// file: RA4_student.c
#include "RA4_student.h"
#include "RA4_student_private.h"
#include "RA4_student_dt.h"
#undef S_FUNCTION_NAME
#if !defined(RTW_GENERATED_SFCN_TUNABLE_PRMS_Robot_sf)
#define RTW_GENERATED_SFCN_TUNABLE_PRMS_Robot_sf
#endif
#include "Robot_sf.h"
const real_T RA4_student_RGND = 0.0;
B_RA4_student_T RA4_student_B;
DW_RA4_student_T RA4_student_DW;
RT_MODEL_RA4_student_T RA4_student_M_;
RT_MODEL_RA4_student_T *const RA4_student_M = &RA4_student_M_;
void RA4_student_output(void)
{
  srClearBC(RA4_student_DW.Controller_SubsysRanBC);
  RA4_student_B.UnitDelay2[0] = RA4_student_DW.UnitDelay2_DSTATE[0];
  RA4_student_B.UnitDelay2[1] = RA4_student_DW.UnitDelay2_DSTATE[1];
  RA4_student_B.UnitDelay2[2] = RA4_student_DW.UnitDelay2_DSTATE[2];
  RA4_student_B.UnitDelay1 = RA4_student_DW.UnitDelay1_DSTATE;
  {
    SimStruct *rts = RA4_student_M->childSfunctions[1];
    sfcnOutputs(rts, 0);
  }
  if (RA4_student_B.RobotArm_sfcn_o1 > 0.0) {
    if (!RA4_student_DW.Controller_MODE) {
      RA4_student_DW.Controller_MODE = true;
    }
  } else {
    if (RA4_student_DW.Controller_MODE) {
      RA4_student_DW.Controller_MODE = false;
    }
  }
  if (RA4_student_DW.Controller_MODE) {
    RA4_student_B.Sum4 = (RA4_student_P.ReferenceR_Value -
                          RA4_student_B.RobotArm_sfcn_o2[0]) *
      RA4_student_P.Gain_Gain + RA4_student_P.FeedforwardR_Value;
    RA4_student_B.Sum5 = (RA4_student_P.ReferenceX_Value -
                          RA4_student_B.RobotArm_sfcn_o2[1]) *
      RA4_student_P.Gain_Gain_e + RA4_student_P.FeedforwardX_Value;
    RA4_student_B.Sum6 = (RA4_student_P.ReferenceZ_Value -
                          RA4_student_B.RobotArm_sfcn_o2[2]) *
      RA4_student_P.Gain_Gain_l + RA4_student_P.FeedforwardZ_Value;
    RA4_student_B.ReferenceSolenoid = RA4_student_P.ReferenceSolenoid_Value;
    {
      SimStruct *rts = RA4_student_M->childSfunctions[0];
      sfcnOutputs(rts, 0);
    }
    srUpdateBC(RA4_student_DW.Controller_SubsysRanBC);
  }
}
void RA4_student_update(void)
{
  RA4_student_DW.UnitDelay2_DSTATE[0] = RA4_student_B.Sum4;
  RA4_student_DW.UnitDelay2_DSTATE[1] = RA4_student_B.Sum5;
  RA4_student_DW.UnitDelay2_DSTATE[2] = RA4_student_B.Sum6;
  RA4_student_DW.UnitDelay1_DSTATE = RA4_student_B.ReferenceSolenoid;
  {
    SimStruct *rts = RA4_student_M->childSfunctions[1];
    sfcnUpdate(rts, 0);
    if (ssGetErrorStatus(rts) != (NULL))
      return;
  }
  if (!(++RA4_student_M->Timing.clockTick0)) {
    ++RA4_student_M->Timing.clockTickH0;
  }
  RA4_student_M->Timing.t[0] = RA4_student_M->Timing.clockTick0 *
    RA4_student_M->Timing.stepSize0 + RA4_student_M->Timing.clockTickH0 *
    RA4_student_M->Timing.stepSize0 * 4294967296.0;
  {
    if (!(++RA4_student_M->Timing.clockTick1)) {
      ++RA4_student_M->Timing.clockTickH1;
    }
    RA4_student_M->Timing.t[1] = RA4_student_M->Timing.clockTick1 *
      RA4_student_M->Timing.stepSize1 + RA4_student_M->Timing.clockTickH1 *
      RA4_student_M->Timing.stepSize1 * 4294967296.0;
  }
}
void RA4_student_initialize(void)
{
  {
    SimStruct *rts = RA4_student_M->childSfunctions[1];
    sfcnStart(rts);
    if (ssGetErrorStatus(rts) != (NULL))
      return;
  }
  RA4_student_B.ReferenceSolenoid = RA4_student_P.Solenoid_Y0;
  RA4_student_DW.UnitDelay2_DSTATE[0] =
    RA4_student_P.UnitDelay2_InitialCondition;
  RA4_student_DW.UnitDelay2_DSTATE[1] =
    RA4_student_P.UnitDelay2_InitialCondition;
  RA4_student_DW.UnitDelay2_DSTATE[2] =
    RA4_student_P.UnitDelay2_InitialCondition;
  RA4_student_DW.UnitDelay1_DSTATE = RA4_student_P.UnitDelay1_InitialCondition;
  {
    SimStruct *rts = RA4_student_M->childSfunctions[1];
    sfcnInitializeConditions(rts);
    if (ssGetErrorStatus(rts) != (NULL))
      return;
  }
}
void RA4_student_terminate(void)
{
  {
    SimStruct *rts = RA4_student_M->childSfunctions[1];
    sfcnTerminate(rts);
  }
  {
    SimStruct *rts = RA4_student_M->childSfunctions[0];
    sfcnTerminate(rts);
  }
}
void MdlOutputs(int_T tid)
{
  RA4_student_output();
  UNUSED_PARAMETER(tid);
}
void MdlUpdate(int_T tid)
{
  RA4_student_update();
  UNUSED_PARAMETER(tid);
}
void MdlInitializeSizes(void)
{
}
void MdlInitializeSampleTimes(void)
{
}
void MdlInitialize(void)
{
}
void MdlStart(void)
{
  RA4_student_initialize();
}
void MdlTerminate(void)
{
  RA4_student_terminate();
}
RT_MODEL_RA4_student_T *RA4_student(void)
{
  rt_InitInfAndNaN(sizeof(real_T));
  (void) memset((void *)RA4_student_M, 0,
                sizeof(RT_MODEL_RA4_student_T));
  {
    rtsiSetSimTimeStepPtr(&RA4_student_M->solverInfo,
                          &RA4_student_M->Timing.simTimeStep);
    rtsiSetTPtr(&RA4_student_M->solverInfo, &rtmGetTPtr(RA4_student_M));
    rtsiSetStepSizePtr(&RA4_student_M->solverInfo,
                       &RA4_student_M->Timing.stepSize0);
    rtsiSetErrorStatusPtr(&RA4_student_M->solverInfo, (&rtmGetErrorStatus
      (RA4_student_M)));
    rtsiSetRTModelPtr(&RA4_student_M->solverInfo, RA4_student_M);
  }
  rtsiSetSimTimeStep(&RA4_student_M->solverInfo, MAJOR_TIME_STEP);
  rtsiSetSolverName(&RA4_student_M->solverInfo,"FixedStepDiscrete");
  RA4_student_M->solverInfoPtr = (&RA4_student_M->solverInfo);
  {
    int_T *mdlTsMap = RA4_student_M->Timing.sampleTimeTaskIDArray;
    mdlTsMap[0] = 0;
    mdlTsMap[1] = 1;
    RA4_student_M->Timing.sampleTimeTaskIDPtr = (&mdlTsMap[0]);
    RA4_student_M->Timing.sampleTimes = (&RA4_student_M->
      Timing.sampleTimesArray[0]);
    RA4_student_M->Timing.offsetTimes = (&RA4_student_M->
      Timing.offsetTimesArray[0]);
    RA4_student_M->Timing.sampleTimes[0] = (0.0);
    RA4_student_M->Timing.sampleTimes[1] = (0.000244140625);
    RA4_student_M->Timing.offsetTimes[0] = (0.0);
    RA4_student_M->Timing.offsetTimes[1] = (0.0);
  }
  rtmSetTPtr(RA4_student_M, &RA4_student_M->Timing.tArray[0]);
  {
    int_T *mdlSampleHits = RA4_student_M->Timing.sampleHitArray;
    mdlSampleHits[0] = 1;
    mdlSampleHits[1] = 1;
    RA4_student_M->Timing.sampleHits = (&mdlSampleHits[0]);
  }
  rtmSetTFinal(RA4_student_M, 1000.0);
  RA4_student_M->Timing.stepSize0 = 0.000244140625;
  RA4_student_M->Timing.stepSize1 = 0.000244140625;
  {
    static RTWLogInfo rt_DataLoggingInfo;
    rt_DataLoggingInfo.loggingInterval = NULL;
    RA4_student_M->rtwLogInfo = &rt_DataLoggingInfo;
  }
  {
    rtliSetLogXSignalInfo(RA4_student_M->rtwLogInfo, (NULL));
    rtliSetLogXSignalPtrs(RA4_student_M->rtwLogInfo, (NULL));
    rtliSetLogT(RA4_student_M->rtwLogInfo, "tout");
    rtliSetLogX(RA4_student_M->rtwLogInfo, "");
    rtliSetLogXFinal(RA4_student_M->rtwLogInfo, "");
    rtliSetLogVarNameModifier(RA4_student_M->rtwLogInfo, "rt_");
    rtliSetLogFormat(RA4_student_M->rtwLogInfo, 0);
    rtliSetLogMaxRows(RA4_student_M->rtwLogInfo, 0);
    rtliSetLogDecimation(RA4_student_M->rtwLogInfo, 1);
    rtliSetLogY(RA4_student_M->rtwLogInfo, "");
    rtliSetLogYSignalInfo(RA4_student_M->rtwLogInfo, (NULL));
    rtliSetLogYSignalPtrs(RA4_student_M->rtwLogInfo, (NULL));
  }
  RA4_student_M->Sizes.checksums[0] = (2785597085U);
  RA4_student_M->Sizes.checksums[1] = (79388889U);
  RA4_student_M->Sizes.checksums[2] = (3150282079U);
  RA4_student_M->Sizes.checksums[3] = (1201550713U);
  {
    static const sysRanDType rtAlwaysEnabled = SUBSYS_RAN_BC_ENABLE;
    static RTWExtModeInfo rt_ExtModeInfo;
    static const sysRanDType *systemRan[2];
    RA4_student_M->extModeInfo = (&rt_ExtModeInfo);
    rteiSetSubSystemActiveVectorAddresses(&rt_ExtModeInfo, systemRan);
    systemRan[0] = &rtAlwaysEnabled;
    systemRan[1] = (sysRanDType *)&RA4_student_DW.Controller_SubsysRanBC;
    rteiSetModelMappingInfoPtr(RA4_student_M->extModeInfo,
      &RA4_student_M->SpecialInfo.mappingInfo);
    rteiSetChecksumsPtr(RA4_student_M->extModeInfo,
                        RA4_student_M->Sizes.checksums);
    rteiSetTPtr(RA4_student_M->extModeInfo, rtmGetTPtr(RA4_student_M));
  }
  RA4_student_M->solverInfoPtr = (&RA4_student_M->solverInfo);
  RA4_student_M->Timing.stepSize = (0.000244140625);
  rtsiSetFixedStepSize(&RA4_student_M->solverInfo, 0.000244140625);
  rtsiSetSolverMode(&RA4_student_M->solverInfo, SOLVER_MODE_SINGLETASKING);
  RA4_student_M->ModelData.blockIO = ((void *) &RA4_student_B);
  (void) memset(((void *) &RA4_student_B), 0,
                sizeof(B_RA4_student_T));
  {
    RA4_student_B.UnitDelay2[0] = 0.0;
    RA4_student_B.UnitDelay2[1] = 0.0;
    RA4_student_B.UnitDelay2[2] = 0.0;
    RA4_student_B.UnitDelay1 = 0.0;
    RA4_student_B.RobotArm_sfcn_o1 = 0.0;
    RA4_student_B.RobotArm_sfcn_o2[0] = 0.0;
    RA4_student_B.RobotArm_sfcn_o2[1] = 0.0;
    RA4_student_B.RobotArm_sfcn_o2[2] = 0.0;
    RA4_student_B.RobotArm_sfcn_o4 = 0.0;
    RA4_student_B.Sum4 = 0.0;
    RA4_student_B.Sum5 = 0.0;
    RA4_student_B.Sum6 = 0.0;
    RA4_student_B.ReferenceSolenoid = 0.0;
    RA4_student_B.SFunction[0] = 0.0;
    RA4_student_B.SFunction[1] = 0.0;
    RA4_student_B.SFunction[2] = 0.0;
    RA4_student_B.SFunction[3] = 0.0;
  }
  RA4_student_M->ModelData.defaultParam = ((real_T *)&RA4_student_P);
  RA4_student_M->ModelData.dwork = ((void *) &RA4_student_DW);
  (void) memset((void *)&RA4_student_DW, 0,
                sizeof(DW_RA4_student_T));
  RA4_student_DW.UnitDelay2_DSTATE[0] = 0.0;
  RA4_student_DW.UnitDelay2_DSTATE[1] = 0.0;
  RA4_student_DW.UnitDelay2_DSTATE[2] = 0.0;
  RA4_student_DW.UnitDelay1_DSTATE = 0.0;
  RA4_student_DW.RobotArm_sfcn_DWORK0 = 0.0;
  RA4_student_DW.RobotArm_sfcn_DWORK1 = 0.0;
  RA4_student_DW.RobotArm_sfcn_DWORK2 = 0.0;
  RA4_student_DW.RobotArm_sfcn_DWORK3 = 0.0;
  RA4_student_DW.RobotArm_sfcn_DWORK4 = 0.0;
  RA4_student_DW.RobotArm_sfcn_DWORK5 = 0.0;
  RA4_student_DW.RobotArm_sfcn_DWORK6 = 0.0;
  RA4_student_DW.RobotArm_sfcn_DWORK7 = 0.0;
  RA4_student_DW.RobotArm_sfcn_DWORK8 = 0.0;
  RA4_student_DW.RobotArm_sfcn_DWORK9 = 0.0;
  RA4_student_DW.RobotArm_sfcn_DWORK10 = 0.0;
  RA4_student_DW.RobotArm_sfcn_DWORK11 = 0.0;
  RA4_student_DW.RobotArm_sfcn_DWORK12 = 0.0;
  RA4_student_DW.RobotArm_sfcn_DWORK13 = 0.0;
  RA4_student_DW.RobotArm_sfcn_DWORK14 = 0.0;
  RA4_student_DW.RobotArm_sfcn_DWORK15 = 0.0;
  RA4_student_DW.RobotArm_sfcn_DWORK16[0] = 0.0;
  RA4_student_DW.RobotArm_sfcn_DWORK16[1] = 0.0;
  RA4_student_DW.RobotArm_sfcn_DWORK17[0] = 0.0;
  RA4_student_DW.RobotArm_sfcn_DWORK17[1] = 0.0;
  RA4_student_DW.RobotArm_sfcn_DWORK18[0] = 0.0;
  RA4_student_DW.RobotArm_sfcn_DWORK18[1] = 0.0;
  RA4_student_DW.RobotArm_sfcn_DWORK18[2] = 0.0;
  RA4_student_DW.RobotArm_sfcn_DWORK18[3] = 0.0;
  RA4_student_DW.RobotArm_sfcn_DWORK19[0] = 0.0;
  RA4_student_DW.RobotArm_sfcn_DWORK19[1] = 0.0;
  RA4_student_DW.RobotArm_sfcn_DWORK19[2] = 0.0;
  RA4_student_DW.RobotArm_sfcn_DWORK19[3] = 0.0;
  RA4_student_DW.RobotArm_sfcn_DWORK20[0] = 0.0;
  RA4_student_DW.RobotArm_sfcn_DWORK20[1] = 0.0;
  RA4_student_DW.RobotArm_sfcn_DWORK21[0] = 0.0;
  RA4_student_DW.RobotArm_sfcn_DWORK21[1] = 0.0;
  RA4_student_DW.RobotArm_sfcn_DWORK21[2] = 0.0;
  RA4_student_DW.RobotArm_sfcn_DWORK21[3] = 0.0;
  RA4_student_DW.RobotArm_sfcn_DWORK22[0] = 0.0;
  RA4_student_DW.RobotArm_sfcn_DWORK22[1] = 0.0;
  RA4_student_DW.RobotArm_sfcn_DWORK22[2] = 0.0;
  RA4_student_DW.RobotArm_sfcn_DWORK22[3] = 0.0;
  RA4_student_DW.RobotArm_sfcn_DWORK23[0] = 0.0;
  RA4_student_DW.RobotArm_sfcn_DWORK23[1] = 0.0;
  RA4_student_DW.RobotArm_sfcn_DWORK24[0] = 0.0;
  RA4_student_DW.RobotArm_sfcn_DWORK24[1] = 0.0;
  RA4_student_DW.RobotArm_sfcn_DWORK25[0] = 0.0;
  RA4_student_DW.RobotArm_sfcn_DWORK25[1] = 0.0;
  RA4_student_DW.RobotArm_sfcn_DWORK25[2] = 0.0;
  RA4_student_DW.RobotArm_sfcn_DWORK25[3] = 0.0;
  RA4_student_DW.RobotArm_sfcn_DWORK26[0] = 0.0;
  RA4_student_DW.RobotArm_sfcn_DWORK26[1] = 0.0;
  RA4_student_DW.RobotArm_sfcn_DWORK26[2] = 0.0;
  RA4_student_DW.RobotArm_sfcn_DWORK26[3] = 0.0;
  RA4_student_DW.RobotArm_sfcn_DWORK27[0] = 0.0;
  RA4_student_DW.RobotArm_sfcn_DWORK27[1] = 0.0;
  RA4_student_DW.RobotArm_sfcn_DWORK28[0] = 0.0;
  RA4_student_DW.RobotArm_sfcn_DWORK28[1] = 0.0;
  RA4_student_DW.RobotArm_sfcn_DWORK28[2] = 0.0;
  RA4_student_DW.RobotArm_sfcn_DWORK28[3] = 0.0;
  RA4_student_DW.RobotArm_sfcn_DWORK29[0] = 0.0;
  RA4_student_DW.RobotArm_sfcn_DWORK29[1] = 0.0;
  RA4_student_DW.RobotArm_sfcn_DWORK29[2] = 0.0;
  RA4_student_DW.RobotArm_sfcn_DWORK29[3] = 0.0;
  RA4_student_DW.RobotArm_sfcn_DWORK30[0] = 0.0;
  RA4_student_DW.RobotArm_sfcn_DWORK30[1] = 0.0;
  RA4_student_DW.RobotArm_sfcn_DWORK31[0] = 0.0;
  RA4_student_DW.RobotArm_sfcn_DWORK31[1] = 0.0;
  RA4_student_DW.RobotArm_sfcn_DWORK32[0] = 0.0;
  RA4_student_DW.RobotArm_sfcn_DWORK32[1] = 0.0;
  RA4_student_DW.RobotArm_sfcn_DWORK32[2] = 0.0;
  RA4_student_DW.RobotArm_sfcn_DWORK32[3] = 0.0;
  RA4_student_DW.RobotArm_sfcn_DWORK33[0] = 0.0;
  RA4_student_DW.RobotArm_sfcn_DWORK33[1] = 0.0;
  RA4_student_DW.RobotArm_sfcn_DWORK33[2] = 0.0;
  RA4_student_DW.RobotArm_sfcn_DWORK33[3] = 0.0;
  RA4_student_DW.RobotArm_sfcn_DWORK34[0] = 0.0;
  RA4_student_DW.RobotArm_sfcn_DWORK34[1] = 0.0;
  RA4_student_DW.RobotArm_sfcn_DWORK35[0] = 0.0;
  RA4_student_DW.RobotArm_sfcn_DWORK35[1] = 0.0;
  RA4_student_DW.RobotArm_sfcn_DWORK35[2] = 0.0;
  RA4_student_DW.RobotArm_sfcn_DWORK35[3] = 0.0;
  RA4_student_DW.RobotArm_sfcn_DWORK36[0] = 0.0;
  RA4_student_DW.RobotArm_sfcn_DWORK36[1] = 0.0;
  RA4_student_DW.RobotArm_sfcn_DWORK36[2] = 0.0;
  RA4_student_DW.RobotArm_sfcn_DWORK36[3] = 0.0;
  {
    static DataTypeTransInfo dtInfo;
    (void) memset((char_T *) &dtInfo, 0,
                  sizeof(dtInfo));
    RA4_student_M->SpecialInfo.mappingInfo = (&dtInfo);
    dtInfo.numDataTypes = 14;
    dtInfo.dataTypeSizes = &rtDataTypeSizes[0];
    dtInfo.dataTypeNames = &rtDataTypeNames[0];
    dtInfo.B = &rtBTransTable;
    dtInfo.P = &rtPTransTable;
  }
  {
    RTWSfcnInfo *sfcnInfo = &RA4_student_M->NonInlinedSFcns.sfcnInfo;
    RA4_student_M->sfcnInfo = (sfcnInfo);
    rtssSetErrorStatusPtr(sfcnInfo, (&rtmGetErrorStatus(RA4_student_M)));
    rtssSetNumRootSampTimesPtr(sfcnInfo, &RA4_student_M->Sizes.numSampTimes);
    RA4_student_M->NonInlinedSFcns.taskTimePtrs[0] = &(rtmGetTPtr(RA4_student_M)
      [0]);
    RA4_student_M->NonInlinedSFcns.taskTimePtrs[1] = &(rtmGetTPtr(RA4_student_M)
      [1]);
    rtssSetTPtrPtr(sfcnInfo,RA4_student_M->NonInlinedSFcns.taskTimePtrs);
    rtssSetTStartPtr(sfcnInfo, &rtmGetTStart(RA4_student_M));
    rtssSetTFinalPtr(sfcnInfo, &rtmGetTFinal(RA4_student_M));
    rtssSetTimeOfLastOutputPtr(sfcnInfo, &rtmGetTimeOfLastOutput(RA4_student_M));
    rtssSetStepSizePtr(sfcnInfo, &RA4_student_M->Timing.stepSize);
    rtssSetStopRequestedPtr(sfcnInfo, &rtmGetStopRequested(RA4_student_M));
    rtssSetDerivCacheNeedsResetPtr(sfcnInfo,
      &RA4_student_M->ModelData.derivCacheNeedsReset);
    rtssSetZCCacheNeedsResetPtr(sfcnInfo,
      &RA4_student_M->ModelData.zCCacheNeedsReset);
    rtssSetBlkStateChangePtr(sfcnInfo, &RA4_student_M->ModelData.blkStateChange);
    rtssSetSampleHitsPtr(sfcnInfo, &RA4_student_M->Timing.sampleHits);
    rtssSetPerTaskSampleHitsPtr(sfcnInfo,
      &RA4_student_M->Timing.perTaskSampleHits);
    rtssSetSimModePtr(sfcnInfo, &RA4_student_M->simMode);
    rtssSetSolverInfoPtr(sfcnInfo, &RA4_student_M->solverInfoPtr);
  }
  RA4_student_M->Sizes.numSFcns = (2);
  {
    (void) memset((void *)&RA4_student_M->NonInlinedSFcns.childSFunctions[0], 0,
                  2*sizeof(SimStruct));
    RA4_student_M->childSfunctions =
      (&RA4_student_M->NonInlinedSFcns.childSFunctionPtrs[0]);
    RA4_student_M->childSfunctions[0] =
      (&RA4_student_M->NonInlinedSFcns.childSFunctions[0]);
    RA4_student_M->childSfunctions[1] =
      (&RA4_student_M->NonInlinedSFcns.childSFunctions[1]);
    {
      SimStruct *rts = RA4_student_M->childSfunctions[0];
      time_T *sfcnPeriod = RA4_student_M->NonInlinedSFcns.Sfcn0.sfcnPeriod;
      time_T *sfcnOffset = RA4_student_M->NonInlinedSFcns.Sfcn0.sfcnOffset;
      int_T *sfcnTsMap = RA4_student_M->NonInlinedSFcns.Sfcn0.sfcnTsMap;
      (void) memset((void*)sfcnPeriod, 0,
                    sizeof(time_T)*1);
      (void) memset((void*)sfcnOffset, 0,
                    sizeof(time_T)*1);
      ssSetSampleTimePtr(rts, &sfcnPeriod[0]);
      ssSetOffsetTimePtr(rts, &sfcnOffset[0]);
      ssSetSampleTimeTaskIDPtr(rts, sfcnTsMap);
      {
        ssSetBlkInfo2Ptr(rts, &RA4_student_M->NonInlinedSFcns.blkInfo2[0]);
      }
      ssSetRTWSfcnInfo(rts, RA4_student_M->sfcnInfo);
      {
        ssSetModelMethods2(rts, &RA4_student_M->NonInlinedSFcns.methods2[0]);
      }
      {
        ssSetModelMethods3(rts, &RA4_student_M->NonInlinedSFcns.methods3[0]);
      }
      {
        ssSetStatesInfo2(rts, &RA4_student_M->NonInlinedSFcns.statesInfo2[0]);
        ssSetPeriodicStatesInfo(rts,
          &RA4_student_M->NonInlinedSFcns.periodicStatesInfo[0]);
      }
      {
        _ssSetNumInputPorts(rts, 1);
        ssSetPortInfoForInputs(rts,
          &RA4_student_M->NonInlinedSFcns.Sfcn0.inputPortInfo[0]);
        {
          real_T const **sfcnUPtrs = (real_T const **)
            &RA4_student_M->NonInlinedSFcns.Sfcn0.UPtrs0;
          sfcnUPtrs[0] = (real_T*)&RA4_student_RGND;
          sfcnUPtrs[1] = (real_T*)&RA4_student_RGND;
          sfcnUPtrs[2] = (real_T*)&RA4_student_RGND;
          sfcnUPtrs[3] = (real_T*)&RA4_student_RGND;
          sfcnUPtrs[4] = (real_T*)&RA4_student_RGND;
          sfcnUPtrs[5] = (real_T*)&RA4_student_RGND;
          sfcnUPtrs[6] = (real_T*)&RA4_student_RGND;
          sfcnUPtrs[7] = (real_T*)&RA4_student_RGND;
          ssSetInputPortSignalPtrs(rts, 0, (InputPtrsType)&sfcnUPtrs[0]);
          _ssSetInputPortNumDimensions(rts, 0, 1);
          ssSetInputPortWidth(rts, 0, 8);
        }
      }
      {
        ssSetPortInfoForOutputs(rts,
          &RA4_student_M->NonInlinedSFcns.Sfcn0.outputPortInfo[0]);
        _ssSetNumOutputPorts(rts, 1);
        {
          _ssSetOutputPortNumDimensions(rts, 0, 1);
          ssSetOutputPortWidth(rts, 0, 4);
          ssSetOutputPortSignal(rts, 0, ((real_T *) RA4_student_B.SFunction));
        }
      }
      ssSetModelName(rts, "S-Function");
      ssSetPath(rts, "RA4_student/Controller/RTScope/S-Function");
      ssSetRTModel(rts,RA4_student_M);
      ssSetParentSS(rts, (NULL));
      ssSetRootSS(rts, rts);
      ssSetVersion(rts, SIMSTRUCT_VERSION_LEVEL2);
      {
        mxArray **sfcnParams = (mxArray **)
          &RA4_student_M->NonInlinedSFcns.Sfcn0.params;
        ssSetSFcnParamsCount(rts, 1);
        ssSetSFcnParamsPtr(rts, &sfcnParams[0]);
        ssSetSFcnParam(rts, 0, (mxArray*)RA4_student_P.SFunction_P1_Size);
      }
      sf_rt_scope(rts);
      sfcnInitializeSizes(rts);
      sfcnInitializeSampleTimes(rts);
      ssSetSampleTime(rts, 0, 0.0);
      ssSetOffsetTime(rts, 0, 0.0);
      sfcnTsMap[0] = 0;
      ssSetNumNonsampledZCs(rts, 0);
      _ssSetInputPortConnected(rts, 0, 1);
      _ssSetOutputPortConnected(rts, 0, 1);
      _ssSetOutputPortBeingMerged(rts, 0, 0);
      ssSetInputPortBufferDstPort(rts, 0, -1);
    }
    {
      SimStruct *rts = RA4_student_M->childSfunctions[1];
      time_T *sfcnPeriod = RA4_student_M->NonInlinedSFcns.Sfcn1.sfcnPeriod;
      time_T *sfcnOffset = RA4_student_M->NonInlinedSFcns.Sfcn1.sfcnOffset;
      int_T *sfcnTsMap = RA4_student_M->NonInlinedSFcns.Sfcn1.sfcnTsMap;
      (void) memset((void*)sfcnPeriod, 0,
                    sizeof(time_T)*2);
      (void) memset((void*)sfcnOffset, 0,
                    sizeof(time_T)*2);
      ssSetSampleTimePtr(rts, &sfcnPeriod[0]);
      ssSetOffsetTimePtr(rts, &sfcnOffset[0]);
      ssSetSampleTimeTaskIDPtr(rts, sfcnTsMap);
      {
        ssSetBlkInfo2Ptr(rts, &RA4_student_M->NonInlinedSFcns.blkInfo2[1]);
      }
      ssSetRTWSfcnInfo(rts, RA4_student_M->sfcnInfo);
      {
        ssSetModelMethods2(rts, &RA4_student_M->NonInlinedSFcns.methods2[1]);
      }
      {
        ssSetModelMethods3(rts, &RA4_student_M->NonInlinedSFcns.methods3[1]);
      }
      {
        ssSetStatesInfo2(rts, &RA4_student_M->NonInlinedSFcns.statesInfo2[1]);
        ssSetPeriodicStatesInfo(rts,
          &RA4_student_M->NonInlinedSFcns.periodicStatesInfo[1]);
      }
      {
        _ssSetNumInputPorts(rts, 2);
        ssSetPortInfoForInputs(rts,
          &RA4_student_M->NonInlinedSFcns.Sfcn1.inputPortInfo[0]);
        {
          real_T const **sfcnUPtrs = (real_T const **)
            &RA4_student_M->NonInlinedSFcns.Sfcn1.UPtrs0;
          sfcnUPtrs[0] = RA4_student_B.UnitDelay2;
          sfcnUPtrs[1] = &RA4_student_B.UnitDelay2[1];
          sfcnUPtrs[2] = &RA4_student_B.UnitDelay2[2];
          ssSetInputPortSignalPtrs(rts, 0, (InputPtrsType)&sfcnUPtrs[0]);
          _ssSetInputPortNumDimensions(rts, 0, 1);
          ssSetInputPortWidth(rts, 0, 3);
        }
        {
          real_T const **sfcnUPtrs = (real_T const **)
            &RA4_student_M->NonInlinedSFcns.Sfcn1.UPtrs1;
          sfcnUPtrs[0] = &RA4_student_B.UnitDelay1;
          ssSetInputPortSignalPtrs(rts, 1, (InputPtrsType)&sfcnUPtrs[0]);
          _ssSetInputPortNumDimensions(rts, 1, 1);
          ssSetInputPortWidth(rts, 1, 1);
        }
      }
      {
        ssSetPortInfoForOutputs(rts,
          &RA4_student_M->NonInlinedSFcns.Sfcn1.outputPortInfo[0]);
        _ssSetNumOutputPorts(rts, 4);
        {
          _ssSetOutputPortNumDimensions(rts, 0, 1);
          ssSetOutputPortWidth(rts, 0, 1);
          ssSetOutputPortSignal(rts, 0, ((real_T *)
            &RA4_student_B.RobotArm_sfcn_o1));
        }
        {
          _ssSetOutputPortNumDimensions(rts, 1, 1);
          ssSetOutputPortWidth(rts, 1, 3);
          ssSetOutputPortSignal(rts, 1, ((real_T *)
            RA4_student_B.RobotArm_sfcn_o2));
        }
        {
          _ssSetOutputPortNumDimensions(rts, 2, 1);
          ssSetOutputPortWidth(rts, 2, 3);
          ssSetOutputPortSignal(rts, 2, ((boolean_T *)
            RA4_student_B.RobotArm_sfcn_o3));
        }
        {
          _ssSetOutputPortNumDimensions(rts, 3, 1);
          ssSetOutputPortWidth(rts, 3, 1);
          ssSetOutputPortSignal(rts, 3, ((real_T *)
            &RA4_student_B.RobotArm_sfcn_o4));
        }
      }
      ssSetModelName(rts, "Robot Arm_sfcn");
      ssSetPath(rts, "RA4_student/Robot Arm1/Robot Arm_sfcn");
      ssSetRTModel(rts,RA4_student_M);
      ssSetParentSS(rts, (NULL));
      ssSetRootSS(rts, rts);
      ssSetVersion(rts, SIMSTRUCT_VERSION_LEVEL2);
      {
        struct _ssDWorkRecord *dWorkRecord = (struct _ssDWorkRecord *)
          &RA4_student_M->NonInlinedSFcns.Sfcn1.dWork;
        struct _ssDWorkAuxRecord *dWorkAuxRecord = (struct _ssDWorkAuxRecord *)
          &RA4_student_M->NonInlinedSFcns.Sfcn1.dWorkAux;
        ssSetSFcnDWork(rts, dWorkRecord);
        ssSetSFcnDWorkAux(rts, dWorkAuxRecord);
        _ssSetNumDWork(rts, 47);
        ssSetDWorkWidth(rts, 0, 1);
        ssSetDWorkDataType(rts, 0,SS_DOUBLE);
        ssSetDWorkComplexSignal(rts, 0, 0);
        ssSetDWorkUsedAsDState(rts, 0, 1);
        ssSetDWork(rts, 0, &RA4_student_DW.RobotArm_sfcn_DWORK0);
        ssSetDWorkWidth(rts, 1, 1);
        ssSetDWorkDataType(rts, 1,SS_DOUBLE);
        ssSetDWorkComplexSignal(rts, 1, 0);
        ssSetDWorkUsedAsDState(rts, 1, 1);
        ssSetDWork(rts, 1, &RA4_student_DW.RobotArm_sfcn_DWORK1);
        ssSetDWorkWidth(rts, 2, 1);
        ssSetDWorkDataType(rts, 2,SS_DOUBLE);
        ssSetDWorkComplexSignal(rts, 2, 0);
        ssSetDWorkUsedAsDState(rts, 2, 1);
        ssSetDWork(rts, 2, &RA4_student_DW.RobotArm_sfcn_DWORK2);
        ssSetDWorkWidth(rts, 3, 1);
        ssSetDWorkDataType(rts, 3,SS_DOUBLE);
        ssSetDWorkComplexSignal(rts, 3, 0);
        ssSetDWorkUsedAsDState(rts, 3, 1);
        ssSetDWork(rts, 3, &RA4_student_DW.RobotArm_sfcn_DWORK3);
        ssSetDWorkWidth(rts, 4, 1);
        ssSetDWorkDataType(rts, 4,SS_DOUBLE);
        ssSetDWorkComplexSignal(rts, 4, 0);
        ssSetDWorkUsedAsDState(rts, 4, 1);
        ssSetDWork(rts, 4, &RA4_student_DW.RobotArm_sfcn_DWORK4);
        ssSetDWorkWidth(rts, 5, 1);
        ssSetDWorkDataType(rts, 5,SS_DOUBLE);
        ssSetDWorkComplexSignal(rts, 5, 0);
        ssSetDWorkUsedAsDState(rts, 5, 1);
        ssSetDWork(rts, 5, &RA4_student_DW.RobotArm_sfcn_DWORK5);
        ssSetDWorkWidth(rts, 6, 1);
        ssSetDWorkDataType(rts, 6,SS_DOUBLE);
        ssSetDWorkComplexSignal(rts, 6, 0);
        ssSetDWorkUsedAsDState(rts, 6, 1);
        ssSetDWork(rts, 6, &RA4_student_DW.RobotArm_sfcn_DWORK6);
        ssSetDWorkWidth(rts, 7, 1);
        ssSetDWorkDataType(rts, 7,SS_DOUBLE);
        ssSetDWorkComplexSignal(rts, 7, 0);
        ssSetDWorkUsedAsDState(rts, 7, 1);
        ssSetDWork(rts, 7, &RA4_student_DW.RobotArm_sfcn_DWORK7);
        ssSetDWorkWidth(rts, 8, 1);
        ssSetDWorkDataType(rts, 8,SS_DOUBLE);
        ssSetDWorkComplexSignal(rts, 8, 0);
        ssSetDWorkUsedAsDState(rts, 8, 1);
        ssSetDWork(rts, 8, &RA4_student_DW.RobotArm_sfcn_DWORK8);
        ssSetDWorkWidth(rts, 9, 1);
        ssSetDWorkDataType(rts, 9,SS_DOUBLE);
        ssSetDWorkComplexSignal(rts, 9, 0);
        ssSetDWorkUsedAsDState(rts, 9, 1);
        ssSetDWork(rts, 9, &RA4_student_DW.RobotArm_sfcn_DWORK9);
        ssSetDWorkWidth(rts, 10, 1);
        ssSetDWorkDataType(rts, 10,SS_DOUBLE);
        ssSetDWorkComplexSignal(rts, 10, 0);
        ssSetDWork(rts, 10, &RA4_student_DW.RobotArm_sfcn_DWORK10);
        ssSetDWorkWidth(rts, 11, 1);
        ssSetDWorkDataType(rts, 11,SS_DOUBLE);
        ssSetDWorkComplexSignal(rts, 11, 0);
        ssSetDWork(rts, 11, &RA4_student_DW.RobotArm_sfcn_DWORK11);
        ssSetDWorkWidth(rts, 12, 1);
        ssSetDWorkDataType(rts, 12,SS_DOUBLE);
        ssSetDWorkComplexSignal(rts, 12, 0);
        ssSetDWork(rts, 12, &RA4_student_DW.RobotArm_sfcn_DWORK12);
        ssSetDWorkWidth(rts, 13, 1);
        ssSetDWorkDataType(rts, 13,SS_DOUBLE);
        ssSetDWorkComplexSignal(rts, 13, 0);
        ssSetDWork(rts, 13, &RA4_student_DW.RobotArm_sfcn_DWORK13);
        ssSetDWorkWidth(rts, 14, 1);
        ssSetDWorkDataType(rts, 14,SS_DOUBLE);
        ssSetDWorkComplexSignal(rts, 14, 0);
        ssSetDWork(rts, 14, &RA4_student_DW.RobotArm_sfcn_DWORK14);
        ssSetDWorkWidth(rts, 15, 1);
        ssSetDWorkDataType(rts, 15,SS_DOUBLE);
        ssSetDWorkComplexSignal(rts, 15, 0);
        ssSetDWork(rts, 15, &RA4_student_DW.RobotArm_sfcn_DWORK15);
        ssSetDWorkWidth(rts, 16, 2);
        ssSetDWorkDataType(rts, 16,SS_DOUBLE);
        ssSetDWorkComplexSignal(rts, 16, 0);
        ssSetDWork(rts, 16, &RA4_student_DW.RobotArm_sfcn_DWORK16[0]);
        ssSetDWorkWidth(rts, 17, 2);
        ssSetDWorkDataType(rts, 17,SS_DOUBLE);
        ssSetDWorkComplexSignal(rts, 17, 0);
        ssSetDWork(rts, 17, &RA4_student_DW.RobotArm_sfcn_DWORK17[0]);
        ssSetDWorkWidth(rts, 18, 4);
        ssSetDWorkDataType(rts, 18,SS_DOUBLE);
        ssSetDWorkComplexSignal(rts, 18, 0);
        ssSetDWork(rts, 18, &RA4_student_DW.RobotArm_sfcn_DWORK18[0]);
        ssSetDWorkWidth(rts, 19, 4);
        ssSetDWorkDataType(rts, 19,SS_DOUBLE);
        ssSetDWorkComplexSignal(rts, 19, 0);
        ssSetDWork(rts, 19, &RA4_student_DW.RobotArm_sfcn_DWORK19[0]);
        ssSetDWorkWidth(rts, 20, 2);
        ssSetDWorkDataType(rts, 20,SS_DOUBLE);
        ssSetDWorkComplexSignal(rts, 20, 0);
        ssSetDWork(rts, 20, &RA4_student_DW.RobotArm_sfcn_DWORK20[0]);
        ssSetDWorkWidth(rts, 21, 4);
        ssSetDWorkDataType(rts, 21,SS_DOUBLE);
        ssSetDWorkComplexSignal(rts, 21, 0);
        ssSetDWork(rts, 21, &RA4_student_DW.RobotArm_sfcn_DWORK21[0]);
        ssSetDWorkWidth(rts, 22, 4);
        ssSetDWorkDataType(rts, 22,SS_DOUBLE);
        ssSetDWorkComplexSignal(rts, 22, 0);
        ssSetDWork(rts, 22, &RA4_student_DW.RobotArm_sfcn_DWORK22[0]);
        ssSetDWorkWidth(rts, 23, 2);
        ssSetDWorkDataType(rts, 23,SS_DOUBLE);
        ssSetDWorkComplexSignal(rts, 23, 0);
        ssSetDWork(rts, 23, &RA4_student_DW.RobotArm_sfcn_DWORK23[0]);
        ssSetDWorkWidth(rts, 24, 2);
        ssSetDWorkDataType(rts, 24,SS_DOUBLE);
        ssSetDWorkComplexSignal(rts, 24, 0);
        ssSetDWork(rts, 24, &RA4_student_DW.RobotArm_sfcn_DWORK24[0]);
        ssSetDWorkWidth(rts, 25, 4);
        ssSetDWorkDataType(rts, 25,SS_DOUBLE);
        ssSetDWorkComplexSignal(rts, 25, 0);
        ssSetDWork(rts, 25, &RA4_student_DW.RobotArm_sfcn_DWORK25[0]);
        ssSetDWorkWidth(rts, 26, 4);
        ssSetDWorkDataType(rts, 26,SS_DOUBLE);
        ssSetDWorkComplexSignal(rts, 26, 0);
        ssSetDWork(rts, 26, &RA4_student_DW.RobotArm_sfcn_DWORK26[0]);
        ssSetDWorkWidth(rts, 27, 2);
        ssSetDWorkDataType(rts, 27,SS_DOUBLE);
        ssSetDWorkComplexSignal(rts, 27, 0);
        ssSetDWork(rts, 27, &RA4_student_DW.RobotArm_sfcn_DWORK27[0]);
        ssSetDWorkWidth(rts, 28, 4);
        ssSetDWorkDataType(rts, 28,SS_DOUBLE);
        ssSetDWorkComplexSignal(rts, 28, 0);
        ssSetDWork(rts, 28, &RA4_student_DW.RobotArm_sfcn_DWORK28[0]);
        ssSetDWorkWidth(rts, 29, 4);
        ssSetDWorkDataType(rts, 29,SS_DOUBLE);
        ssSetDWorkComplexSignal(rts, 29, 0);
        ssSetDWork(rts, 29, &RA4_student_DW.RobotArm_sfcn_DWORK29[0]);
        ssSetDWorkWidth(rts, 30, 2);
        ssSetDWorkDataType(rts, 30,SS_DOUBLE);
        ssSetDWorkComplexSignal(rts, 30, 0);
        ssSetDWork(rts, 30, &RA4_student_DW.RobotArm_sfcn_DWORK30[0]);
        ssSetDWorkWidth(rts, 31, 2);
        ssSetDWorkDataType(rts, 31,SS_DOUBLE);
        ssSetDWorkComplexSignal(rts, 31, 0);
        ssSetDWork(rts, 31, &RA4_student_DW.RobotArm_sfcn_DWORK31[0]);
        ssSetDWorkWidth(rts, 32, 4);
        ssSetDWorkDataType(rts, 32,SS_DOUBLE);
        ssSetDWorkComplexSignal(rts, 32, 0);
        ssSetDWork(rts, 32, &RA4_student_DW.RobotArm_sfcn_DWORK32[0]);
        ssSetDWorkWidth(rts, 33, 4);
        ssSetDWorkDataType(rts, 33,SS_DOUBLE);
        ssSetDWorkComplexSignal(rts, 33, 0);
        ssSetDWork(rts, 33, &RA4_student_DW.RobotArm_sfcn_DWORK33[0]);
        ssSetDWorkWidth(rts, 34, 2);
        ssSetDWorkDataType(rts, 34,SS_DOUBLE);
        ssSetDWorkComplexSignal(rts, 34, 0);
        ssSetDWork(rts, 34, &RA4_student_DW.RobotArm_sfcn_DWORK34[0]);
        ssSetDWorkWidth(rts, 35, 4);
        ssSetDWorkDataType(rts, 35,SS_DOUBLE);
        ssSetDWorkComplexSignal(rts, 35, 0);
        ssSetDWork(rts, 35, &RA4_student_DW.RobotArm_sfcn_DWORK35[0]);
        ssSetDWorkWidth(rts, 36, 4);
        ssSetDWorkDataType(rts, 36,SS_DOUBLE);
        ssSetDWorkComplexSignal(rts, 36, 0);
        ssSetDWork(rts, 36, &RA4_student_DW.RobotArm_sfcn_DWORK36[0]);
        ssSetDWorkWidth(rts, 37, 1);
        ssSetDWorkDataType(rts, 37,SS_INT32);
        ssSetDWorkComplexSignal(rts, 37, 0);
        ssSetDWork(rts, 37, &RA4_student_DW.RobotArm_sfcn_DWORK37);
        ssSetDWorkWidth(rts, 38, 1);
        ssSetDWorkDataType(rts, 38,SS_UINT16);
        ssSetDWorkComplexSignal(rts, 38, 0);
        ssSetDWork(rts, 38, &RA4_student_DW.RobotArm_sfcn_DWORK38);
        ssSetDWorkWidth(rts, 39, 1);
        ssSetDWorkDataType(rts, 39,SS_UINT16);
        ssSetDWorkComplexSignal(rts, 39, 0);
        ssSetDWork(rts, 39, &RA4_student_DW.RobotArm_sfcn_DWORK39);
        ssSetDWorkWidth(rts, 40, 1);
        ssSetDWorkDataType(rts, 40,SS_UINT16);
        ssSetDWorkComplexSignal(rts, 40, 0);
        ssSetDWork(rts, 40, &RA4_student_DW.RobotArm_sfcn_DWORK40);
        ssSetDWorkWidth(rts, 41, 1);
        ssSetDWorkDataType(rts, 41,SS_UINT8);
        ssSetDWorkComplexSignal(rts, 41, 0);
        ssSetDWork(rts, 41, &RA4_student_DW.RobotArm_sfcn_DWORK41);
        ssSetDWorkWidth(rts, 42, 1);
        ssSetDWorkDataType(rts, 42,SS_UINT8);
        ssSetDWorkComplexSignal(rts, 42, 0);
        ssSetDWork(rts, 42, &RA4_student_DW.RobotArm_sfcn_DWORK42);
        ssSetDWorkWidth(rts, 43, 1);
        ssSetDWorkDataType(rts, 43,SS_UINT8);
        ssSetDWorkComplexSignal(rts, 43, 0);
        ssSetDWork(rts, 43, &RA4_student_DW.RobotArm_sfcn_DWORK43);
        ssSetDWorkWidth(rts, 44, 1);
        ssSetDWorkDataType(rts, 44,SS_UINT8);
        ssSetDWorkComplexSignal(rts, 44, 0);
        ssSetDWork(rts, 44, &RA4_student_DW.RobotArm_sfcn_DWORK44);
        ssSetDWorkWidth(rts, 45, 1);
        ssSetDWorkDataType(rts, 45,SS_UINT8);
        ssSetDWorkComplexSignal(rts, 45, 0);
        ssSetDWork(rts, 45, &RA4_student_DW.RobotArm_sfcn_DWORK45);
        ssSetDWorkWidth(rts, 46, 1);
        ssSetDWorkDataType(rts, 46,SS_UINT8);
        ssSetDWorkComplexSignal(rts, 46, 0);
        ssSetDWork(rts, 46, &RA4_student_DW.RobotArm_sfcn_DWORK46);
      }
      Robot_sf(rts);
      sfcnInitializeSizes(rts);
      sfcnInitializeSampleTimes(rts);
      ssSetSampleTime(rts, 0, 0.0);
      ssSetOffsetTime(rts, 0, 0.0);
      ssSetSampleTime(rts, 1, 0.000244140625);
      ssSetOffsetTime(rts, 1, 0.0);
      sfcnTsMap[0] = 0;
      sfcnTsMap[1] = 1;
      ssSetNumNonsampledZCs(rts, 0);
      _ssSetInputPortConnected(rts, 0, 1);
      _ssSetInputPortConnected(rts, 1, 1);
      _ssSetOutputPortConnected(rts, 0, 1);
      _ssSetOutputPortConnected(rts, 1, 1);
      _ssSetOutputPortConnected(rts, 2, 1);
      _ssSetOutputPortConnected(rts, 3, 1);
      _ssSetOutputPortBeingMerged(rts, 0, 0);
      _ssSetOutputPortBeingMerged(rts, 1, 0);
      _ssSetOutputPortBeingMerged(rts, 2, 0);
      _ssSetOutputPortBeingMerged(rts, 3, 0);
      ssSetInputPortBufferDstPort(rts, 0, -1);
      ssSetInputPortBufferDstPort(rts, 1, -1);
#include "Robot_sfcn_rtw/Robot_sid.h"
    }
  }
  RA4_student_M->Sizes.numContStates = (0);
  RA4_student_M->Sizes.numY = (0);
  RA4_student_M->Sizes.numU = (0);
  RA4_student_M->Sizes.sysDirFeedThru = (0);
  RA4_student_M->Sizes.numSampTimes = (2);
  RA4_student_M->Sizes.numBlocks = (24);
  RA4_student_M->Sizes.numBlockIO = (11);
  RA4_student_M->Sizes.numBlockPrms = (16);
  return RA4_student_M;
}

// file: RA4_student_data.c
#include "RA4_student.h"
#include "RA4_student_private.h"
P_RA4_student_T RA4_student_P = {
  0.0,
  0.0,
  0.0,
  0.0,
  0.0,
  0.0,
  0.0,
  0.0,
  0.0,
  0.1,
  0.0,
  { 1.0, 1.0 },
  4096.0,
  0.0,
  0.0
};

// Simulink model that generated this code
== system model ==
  UnitDelay2 : UnitDelay  <- 1: Controller
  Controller : Subsystem  <- 1: RobotArm_sfcn/2, Enable: RobotArm_sfcn
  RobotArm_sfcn : S-Function  FunctionName=Robot_sf  <- 1: UnitDelay2, 2: UnitDelay1
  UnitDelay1 : UnitDelay  <- 1: Controller/2
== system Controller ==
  Inport#1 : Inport
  EnablePort#1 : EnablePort
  Outport#1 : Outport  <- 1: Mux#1
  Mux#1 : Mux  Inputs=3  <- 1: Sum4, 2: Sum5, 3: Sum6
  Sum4 : Sum  Inputs=++  <- 1: FeedforwardR, 2: Gain
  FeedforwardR : Constant  Value=0
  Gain : Gain  Gain=0  <- 1: Sum#1
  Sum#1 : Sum  Inputs=+-  <- 1: ReferenceR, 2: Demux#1
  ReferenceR : Constant  Value=0
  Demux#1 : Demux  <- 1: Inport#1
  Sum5 : Sum  Inputs=++  <- 1: FeedforwardX, 2: Gain#1
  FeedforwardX : Constant  Value=0
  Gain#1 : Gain  Gain=0  <- 1: Sum#2
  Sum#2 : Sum  Inputs=+-  <- 1: ReferenceX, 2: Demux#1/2
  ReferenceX : Constant  Value=0
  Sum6 : Sum  Inputs=++  <- 1: FeedforwardZ, 2: Gain#2
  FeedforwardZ : Constant  Value=0.1
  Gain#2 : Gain  Gain=0  <- 1: Sum#3
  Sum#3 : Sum  Inputs=+-  <- 1: ReferenceZ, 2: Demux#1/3
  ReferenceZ : Constant  Value=0
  Solenoid : Outport  InitialOutput=0  <- 1: ReferenceSolenoid
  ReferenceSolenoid : Constant  Value=0
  SFunction : S-Function  FunctionName=sf_rt_scope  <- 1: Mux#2
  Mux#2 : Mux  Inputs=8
